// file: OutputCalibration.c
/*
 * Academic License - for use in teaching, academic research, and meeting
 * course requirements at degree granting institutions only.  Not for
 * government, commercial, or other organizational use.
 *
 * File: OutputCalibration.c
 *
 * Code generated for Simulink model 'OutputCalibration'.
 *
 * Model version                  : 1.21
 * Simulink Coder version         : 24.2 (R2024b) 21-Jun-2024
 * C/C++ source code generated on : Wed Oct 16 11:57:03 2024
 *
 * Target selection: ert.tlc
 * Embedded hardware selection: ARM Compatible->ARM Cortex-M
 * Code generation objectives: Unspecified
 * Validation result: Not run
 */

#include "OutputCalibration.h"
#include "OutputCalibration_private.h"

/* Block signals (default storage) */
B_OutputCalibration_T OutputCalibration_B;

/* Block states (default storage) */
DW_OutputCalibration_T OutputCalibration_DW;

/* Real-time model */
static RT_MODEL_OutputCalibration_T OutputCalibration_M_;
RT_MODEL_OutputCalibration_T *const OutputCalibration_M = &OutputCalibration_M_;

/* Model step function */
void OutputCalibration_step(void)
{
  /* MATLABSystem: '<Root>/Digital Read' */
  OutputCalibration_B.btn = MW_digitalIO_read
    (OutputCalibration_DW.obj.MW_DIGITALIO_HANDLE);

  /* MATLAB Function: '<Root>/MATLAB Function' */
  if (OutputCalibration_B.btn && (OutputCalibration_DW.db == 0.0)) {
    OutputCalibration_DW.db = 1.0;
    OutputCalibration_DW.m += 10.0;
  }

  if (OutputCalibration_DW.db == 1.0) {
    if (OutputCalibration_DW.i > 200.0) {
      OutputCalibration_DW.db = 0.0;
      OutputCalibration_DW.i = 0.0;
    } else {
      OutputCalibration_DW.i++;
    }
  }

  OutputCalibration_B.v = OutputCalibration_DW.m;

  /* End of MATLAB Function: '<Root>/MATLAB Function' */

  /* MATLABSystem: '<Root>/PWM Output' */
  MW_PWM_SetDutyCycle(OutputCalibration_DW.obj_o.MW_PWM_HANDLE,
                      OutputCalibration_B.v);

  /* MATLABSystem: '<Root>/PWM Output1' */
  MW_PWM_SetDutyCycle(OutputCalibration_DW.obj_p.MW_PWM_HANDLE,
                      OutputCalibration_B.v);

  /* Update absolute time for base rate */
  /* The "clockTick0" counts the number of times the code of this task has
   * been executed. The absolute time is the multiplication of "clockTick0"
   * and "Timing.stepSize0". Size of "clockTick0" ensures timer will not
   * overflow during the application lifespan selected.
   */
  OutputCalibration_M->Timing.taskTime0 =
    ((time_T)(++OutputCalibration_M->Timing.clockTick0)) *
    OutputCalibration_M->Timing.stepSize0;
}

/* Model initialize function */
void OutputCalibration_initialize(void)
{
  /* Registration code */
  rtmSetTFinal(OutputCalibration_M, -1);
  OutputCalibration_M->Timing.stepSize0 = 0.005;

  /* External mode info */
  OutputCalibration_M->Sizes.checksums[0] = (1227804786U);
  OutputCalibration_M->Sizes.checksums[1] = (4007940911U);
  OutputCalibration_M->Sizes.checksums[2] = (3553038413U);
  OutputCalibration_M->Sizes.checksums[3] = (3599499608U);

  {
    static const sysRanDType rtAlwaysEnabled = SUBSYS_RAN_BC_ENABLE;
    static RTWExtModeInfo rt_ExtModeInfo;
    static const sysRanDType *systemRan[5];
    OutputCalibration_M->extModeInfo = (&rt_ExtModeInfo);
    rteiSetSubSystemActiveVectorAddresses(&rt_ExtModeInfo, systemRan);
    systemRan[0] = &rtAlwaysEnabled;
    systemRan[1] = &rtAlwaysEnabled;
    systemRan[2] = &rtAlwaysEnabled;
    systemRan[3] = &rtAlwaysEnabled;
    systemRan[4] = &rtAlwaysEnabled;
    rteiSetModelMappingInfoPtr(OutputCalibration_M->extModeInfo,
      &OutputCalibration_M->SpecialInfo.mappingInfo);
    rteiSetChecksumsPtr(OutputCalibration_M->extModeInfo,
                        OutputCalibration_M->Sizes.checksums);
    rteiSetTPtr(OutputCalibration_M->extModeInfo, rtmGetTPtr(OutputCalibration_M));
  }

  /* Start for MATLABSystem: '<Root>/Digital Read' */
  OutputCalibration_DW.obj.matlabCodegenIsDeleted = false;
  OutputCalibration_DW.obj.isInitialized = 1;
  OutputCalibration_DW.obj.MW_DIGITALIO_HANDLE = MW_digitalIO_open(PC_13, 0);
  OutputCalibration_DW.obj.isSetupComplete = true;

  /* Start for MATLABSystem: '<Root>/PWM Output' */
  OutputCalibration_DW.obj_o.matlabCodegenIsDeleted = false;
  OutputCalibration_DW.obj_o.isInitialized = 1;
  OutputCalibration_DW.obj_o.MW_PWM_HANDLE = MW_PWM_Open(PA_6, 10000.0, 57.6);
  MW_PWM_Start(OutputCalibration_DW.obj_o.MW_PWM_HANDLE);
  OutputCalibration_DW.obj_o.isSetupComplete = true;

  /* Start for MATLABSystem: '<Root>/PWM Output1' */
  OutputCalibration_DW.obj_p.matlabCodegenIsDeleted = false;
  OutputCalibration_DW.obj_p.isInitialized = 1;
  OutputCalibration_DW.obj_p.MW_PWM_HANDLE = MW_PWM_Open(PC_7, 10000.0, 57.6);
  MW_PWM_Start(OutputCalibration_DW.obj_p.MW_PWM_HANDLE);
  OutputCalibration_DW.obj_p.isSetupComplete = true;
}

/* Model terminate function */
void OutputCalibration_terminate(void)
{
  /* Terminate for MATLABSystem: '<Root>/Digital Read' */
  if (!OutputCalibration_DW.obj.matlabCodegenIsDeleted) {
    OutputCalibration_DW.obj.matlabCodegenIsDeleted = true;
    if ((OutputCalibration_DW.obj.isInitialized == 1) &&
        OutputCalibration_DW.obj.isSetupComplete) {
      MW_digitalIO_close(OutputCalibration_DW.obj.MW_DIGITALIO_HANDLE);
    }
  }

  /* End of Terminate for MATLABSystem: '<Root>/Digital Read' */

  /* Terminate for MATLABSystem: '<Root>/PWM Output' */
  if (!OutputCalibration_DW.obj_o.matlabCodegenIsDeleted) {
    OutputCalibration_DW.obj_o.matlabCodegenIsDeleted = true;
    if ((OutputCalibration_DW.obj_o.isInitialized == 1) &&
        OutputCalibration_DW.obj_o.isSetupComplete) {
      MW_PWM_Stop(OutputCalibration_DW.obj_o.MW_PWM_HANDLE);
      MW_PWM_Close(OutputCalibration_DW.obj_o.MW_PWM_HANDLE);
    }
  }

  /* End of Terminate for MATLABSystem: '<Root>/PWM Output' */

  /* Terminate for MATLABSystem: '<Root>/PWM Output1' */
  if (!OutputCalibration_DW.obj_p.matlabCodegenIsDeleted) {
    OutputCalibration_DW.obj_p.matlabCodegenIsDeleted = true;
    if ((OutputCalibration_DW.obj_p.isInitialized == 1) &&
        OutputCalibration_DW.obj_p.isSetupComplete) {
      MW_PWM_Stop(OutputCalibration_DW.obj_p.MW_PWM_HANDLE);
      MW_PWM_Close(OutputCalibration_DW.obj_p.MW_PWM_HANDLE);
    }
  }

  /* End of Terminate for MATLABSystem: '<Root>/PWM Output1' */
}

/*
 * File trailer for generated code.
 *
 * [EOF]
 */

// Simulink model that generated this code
simulink model "OutputCalibration"  (R2024b)
settings: Solver=FixedStepAuto  StartTime=0.0  StopTime=inf  FixedStep=1/200  RelTol=1e-3  EnableMultiTasking=on
libraries: mbedblockslib x3

== system OutputCalibration ==
  Digital Read : mbedblockslib/Digital Read  Pin=PC_13  Direction=input  SampleTime=-1
  MATLAB Function : MATLAB Function  TreatAsAtomicUnit=on
  PWM Output : mbedblockslib/PWM Output  Pin=PA_6  EnableInputFrequency=off  InitialFrequency=10000  InitialDutyCycle=57.6  NotificationType=None
  PWM Output1 : mbedblockslib/PWM Output  Pin=PC_7  EnableInputFrequency=off  InitialFrequency=10000  InitialDutyCycle=57.6  NotificationType=None
  Scope : Scope
  wires:
  Digital Read/1 -> MATLAB Function/1(user_button)  "btn"
  MATLAB Function/1(v) -> PWM Output1/1, Scope/1, PWM Output/1  "out"

== matlab function OutputCalibration/MATLAB Function ==
function v = fcn(user_button)

persistent m db i;
Fs = 200;

if isempty(m)
    m = 0;
    i = 0;
    db = 0;
end

if user_button == 1
    if db == 0
        db = 1;
        m = m + 10;
    end
end

if db == 1
    if i > 1*Fs
        db = 0;
        i = 0;
    else
        i = i + 1;
    end
end

v = m;
end
